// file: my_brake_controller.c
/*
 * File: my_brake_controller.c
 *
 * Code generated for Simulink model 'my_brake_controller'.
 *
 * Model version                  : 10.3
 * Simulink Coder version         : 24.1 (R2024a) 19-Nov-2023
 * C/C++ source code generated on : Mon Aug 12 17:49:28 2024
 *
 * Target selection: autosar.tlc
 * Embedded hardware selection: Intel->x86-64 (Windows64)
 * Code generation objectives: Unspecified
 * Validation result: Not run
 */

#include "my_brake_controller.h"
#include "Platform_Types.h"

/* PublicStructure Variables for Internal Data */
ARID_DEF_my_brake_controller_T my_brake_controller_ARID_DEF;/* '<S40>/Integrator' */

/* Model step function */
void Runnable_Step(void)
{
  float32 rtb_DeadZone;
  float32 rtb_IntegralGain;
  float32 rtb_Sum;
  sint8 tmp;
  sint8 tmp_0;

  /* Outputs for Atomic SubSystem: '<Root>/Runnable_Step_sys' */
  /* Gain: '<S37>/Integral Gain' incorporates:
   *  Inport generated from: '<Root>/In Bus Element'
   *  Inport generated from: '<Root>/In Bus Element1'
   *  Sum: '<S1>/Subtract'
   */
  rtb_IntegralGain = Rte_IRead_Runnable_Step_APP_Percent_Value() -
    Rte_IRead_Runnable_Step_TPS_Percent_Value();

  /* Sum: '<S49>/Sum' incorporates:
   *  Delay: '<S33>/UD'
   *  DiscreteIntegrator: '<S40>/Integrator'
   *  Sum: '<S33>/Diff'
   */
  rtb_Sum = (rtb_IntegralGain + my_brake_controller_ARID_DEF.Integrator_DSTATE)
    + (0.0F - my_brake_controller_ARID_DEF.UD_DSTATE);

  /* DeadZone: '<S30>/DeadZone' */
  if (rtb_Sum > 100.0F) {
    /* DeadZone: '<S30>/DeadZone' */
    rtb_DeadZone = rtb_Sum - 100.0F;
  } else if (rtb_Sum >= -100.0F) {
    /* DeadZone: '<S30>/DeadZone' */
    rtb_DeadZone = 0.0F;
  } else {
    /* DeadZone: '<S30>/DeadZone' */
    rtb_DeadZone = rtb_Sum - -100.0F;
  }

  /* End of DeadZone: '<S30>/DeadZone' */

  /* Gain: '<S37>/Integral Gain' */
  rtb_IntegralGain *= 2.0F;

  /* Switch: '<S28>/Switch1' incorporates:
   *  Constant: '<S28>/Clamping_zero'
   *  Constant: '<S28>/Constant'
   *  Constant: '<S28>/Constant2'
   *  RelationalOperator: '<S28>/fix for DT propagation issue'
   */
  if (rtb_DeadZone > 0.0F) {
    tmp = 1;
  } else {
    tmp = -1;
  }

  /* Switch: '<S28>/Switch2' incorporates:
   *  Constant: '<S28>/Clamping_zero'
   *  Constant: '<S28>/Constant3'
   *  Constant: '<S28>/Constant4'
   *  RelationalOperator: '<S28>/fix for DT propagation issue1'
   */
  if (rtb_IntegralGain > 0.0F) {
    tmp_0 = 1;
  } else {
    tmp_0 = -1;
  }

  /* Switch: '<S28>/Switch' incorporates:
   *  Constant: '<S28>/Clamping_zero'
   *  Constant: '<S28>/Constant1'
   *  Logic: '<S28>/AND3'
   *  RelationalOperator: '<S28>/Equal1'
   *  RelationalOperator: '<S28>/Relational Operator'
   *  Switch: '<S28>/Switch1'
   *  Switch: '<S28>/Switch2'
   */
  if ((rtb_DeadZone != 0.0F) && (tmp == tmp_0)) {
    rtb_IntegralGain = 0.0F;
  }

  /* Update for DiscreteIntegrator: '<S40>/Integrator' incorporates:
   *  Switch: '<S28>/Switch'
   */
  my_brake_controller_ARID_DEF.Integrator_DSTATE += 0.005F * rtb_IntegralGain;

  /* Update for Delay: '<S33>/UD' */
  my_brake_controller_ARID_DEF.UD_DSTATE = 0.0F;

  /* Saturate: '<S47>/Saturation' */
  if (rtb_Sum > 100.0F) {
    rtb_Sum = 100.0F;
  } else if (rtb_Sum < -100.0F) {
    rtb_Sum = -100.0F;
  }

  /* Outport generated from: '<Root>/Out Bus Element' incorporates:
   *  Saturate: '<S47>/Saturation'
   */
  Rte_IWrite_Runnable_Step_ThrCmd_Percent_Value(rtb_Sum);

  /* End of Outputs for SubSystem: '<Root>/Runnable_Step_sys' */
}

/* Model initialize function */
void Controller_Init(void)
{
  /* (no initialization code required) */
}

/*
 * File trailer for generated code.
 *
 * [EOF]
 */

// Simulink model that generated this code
simulink model "my_brake_controller"  (R2024a)
settings: Solver=FixedStepDiscrete  StartTime=0.0  StopTime=10.0  FixedStep=0.005  RelTol=1e-3
libraries: slpidlib x1

== system my_brake_controller ==
  In Bus Element1 : Inport  PortName=TPS_Percent  Element=Value
  In Bus Element : Inport  Port=2  PortName=APP_Percent  Element=Value
  Runnable_Step_sys : Subsystem  TreatAsAtomicUnit=on  SystemSampleTime=0.005
  Out Bus Element : Outport  PortName=ThrCmd_Percent  Element=Value
  wires:
  In Bus Element/1 -> Runnable_Step_sys/2(APP_Percent_Value_read)
  In Bus Element1/1 -> Runnable_Step_sys/1(TPS_Percent_Value_read)
  Runnable_Step_sys/1(ThrCmd_Percent_Value_write) -> Out Bus Element/1

== system my_brake_controller/Runnable_Step_sys ==
  TPS_Percent_Value_read : Inport
  APP_Percent_Value_read : Inport  Port=2
  Discrete PID Controller : slpidlib/PID Controller  Controller=PID  Form=Parallel  TimeDomain=Discrete-time  UseExternalTs=off  SampleTime=-1  IntegratorMethod=Forward Euler  FilterMethod=Forward Euler  ControllerParametersSource=internal  P=1  I=2  UseKiTs=off  D=0  UseExternalDerivativeSource=off  N=100  UseFilter=off  TunerSelectOption=Transfer Function Based (PID Tuner App)  InitialConditionSource=internal  InitialConditionForIntegrator=0  InitialConditionForFilter=0  DifferentiatorICPrevScaledInput=0  ExternalReset=none  TrackingMode=off  Kt=1  LimitOutput=on  SatLimitsSource=internal  UpperSaturationLimit=100  LowerSaturationLimit=-100  LinearizeAsGain=off  AntiWindupMode=clamping  Kb=1  LimitIntegrator=off  UpperIntegratorSaturationLimit=inf  LowerIntegratorSaturationLimit=-inf  POutMin=[]  POutMax=[]  IOutMin=[]  IOutMax=[]  DOutMin=[]  DOutMax=[]  NOutMin=[]  NOutMax=[]  SumOutMin=[]  SumOutMax=[]  SaturationOutMin=[]  SaturationOutMax=[]  PParamMin=[]  PParamMax=[]  IParamMin=[]  IParamMax=[]  DParamMin=[]  DParamMax=[]  NParamMin=[]  NParamMax=[]  KbParamMin=[]  KbParamMax=[]  KtParamMin=[]  KtParamMax=[]  KbOutMin=[]  KbOutMax=[]  KtOutMin=[]  KtOutMax=[]  IntegratorOutMin=[]  IntegratorOutMax=[]  FilterOutMin=[]  FilterOutMax=[]  SumI1OutMin=[]  SumI1OutMax=[]  SumI2OutMin=[]  SumI2OutMax=[]  SumI3OutMin=[]  SumI3OutMax=[]  SumI4OutMin=[]  SumI4OutMax=[]  SumDOutMin=[]  SumDOutMax=[]  DifferentiatorOutMin=[]  DifferentiatorOutMax=[]  FilterDiffOutCoefMin=[]  FilterDiffOutCoefMax=[]  ReciprocalOutMin=[]  ReciprocalOutMax=[]  SumDenOutMin=[]  SumDenOutMax=[]  SumNumOutMin=[]  SumNumOutMax=[]  DivideOutMin=[]  DivideOutMax=[]  UdiffTsProdOutMin=[]  UdiffTsProdOutMax=[]  NTsProdOutMin=[]  NTsProdOutMax=[]  UintegralTsProdOutMin=[]  UintegralTsProdOutMax=[]  UngainTsProdOutMin=[]  UngainTsProdOutMax=[]  ClampingZeroOutDataTypeStr=Inherit: Inherit via back propagation  ClampingZeroOutMin=[]  ClampingZeroOutMax=[]  FilterDenConstantOutDataTypeStr=Inherit: Inherit via back propagation  FilterDenConstantOutMin=[]  FilterDenConstantOutMax=[]  PCopyOutDataTypeStr=Inherit: Inherit via back propagation  PCopyOutMin=[]  PCopyOutMax=[]  NCopyOutDataTypeStr=Inherit: Inherit via back propagation  NCopyOutMin=[]  NCopyOutMax=[]  IntegratorContinuousStateAttributes=''  IntegratorStateMustResolveToSignalObject=off  IntegratorRTWStateStorageClass=Auto  FilterContinuousStateAttributes=''  FilterStateMustResolveToSignalObject=off  FilterRTWStateStorageClass=Auto  ParallelPVariant=InternalParameters  IdealPVariant=Disabled  IVariant=InternalParameters  DVariant=InternalParameters  IntegratorVariant=Discrete  SatVariant=Enabled  AWVariant=DiscClampingParallel  PCopyVariant=Disabled  TRVariant=Disabled  FdbkBlocksVariant=Forward  IdealPFdbkVariant=Disabled  SatFdbkVariant=Disabled  DerivativeFilterVariant=Differentiator  NVariant=Passthrough  NCopyVariant=Disabled_SignalSpec  FilterICVariant=InternalICsDifferentiator  IntegratorICVariant=InternalICs  ExternalResetVariant=Disabled  TRSumVariant=Passthrough  SumFdbkVariant=Disabled  SumVariant=Sum_PID  TsampFilterVariant=InternalTs  TsampNgainVariant=Passthrough  TsampIntegralVariant=Disabled_SignalSpec  ExternalSaturationOutDataTypeStr=Inherit: Same as second input  DerivativeSourceVariant=ErrorSignal
  Scope : Scope  NumInputPorts=4
  Subtract : Sum  Inputs=+-
  ThrCmd_Percent_Value_write : Outport  VectorParamsAs1DForOutWhenUnconnected=off
  wires:
  TPS_Percent_Value_read/1 -> Scope/3, Subtract/2
  APP_Percent_Value_read/1 -> Scope/2, Subtract/1
  Discrete PID Controller/1 -> Scope/4, ThrCmd_Percent_Value_write/1
  Subtract/1 -> Scope/1, Discrete PID Controller/1  "error"
